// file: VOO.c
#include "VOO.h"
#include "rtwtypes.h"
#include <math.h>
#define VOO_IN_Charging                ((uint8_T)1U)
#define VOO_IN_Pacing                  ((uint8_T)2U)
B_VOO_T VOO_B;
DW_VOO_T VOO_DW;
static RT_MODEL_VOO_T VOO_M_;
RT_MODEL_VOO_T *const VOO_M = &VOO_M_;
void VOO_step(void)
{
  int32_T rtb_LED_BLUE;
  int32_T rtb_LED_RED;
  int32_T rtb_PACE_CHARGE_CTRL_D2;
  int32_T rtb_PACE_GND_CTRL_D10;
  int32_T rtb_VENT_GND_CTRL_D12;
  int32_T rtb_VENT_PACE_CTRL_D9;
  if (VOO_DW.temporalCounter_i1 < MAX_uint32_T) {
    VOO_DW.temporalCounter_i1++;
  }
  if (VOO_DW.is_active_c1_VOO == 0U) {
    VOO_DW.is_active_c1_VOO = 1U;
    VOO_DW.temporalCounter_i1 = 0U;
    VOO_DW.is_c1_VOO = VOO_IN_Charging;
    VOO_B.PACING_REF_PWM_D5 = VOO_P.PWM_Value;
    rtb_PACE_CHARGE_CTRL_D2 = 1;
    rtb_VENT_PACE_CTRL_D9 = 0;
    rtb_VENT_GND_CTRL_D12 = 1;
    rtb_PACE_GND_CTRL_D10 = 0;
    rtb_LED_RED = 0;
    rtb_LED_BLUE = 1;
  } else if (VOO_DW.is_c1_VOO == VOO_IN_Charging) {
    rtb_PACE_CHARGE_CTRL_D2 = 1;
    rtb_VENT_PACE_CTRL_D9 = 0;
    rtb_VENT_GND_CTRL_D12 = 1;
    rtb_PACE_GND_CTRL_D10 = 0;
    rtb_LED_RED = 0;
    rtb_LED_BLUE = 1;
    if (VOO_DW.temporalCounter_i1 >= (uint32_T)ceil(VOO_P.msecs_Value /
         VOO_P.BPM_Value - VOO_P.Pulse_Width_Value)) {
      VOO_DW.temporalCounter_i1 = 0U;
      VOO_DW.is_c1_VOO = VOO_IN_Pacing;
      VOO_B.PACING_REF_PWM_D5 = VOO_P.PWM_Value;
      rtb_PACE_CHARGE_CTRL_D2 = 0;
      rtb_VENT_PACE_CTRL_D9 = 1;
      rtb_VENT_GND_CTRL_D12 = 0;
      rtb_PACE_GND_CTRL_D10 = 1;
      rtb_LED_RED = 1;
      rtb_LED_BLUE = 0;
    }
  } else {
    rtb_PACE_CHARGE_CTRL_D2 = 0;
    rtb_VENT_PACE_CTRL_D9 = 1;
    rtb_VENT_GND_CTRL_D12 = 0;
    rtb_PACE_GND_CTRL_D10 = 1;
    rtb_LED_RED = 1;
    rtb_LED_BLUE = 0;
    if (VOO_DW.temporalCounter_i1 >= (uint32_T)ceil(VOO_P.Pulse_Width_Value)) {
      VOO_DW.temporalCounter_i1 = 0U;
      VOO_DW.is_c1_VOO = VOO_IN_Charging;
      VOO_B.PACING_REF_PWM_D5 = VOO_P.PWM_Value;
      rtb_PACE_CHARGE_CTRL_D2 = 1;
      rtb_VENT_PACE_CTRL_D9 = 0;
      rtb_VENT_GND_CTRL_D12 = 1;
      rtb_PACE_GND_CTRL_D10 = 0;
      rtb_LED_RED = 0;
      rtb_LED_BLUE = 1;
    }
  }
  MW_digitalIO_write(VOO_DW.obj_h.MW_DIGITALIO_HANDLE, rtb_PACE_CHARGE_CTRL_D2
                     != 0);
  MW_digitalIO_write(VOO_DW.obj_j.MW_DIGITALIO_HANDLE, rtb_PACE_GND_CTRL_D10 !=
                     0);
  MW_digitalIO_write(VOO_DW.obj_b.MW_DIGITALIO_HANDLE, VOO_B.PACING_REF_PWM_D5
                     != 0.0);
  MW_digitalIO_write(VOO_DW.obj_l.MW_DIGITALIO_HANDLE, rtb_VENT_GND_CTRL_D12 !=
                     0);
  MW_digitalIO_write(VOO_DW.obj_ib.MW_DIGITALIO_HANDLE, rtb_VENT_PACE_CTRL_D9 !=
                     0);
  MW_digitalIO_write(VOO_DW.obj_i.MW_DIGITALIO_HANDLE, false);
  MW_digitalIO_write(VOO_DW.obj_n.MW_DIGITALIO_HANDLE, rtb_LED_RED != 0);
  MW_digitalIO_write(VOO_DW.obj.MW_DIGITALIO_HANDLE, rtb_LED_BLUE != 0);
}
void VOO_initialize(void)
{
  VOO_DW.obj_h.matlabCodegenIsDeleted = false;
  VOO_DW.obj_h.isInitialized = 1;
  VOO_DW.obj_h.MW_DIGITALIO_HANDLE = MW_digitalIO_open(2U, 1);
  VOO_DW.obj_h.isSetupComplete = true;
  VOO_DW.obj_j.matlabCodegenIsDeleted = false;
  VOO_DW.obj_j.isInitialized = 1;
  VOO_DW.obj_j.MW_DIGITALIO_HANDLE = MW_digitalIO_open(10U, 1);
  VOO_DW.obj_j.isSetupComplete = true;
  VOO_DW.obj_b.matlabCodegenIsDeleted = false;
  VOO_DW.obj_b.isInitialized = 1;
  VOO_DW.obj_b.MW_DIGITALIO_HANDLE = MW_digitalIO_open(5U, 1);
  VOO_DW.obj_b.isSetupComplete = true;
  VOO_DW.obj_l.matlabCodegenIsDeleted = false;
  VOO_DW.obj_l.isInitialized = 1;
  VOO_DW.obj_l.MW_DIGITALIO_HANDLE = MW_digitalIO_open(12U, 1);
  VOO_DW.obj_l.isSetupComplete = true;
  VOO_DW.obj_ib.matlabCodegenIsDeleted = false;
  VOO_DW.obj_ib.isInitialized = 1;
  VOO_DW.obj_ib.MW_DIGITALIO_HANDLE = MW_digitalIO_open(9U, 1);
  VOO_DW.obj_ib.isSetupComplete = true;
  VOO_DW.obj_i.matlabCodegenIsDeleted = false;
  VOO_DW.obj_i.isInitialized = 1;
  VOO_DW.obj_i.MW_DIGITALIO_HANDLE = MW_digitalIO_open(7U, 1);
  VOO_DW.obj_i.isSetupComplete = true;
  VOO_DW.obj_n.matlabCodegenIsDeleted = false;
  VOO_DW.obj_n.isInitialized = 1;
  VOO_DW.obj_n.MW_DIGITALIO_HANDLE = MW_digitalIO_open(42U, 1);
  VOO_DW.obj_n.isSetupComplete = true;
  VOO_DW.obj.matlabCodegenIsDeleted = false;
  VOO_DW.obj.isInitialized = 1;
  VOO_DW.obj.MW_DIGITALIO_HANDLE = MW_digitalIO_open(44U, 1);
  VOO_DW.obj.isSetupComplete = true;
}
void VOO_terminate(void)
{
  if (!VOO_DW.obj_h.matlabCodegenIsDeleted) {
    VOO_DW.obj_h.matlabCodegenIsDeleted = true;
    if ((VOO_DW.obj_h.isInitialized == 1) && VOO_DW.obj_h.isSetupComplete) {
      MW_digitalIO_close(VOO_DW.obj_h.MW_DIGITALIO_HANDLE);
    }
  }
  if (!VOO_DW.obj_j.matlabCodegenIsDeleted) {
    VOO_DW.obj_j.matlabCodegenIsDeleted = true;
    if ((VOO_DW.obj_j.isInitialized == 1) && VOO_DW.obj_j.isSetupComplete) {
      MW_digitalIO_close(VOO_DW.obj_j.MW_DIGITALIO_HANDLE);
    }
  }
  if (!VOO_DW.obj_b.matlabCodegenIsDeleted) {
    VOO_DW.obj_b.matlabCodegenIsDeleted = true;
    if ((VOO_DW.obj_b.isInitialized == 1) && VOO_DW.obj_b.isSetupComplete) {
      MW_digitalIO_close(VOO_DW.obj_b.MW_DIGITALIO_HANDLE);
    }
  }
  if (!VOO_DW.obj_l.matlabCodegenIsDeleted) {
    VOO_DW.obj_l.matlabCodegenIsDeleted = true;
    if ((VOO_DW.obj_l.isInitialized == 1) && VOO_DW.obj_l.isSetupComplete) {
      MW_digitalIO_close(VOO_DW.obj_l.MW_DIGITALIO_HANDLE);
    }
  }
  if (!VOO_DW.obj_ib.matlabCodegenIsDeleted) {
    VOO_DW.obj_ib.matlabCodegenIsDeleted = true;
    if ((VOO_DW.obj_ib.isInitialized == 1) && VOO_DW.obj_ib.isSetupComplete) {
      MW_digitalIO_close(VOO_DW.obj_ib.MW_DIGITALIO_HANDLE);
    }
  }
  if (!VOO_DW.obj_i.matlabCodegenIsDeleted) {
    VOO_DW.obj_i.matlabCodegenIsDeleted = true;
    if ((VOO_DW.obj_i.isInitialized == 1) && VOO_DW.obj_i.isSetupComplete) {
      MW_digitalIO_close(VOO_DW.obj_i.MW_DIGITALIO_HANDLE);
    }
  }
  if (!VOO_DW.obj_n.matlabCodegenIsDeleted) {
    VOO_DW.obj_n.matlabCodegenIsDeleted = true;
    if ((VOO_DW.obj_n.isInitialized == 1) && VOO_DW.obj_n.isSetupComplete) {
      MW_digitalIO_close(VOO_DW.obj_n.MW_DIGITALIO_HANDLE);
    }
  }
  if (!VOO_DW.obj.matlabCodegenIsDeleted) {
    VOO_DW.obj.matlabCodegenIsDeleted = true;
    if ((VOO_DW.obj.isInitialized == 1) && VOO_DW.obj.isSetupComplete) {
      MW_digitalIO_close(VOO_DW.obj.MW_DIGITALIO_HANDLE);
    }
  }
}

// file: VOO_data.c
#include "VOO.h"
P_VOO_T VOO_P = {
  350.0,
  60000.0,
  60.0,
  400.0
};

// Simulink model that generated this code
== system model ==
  DigitalWrite#1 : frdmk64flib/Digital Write  <- 1: VOO
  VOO : Stateflow chart  <- 1: PWM, 2: Product#1, 3: Pulse_Width
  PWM : Constant  Value=350
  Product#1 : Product  Inputs=*/  <- 1: msecs, 2: BPM
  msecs : Constant  Value=60000
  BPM : Constant  Value=60
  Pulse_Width : Constant  Value=400
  DigitalWrite#2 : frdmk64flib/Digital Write  <- 1: VOO/2
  DigitalWrite#3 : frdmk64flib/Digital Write  <- 1: VOO/3
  DigitalWrite#4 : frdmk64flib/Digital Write  <- 1: VOO/4
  DigitalWrite#5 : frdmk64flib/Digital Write  <- 1: VOO/5
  DigitalWrite#6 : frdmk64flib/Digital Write  <- 1: VOO/6
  DigitalWrite#7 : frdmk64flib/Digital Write  <- 1: VOO/7
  DigitalWrite#8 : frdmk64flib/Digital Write  <- 1: VOO/8
== stateflow chart VOO ==
  state Charging
    entry:
    PACING_REF_PWM_D5 = data;
    PACE_CHARGE_CTRL_D2 = 1;
    VENT_PACE_CTRL_D9 = 0;
    VENT_GND_CTRL_D12 = 1;
    PACE_GND_CTRL_D10 = 0;
    Z_VENT_CTRL_D7 = 0;
    LED_RED = 0;
    LED_BLUE = 1;
  state Pacing
    entry:
    PACING_REF_PWM_D5 = data;
    PACE_CHARGE_CTRL_D2 = 0;
    VENT_PACE_CTRL_D9 = 1;
    VENT_GND_CTRL_D12 = 0;
    PACE_GND_CTRL_D10 = 1;
    Z_VENT_CTRL_D7 = 0;
    LED_RED = 1;
    LED_BLUE = 0;
  (default) -> Charging
  Charging -> Pacing : [after(Pace_Period - Pulse_Width,msec)]
  Pacing -> Charging : [after(Pulse_Width,msec)]
  data: data input; PACE_CHARGE_CTRL_D2 output; PACE_GND_CTRL_D10 output; PACING_REF_PWM_D5 output; VENT_GND_CTRL_D12 output; VENT_PACE_CTRL_D9 output; Z_VENT_CTRL_D7 output; LED_RED output; LED_BLUE output; Pace_Period input; Pulse_Width input
